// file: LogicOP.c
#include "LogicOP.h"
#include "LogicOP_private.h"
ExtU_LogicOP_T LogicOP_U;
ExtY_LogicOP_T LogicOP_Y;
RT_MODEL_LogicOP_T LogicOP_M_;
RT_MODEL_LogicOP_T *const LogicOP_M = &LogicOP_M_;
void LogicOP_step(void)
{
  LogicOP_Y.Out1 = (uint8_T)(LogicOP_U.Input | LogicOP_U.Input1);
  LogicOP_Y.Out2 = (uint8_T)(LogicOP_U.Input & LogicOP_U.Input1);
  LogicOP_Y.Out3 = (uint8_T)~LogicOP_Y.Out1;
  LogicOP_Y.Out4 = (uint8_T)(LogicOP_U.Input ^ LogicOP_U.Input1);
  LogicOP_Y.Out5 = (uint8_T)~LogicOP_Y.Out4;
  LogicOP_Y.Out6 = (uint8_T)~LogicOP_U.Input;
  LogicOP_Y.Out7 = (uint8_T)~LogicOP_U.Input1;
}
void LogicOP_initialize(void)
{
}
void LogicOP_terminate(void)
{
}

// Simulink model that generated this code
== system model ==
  Input : Inport
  Input1 : Inport
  Out1 : Outport  <- 1: BitwiseOperator#1
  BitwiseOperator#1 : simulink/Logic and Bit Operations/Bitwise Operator  logicop=OR  BitMask=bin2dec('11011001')  <- 1: Input, 2: Input1
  Out2 : Outport  <- 1: BitwiseOperator#2
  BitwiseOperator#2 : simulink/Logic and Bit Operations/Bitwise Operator  logicop=AND  BitMask=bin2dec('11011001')  <- 1: Input, 2: Input1
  Out3 : Outport  <- 1: BitwiseOperator#3
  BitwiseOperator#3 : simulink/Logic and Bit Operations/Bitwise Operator  logicop=NOR  BitMask=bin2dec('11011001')  <- 1: Input, 2: Input1
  Out4 : Outport  <- 1: BitwiseOperator#4
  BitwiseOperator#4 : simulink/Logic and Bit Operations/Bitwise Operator  logicop=XOR  BitMask=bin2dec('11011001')  <- 1: Input, 2: Input1
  Out5 : Outport  <- 1: BitwiseOperator#5
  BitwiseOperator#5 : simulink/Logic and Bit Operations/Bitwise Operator  logicop=NOT  BitMask=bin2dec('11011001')  <- 1: BitwiseOperator#6
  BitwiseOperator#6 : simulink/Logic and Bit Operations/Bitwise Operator  logicop=XOR  BitMask=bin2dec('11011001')  <- 1: Input, 2: Input1
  Out6 : Outport  <- 1: BitwiseOperator#7
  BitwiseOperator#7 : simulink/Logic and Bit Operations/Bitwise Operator  logicop=NOT  BitMask=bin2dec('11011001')  <- 1: Input
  Out7 : Outport  <- 1: BitwiseOperator#8
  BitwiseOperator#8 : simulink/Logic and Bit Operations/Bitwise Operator  logicop=NOT  BitMask=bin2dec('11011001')  <- 1: Input1
